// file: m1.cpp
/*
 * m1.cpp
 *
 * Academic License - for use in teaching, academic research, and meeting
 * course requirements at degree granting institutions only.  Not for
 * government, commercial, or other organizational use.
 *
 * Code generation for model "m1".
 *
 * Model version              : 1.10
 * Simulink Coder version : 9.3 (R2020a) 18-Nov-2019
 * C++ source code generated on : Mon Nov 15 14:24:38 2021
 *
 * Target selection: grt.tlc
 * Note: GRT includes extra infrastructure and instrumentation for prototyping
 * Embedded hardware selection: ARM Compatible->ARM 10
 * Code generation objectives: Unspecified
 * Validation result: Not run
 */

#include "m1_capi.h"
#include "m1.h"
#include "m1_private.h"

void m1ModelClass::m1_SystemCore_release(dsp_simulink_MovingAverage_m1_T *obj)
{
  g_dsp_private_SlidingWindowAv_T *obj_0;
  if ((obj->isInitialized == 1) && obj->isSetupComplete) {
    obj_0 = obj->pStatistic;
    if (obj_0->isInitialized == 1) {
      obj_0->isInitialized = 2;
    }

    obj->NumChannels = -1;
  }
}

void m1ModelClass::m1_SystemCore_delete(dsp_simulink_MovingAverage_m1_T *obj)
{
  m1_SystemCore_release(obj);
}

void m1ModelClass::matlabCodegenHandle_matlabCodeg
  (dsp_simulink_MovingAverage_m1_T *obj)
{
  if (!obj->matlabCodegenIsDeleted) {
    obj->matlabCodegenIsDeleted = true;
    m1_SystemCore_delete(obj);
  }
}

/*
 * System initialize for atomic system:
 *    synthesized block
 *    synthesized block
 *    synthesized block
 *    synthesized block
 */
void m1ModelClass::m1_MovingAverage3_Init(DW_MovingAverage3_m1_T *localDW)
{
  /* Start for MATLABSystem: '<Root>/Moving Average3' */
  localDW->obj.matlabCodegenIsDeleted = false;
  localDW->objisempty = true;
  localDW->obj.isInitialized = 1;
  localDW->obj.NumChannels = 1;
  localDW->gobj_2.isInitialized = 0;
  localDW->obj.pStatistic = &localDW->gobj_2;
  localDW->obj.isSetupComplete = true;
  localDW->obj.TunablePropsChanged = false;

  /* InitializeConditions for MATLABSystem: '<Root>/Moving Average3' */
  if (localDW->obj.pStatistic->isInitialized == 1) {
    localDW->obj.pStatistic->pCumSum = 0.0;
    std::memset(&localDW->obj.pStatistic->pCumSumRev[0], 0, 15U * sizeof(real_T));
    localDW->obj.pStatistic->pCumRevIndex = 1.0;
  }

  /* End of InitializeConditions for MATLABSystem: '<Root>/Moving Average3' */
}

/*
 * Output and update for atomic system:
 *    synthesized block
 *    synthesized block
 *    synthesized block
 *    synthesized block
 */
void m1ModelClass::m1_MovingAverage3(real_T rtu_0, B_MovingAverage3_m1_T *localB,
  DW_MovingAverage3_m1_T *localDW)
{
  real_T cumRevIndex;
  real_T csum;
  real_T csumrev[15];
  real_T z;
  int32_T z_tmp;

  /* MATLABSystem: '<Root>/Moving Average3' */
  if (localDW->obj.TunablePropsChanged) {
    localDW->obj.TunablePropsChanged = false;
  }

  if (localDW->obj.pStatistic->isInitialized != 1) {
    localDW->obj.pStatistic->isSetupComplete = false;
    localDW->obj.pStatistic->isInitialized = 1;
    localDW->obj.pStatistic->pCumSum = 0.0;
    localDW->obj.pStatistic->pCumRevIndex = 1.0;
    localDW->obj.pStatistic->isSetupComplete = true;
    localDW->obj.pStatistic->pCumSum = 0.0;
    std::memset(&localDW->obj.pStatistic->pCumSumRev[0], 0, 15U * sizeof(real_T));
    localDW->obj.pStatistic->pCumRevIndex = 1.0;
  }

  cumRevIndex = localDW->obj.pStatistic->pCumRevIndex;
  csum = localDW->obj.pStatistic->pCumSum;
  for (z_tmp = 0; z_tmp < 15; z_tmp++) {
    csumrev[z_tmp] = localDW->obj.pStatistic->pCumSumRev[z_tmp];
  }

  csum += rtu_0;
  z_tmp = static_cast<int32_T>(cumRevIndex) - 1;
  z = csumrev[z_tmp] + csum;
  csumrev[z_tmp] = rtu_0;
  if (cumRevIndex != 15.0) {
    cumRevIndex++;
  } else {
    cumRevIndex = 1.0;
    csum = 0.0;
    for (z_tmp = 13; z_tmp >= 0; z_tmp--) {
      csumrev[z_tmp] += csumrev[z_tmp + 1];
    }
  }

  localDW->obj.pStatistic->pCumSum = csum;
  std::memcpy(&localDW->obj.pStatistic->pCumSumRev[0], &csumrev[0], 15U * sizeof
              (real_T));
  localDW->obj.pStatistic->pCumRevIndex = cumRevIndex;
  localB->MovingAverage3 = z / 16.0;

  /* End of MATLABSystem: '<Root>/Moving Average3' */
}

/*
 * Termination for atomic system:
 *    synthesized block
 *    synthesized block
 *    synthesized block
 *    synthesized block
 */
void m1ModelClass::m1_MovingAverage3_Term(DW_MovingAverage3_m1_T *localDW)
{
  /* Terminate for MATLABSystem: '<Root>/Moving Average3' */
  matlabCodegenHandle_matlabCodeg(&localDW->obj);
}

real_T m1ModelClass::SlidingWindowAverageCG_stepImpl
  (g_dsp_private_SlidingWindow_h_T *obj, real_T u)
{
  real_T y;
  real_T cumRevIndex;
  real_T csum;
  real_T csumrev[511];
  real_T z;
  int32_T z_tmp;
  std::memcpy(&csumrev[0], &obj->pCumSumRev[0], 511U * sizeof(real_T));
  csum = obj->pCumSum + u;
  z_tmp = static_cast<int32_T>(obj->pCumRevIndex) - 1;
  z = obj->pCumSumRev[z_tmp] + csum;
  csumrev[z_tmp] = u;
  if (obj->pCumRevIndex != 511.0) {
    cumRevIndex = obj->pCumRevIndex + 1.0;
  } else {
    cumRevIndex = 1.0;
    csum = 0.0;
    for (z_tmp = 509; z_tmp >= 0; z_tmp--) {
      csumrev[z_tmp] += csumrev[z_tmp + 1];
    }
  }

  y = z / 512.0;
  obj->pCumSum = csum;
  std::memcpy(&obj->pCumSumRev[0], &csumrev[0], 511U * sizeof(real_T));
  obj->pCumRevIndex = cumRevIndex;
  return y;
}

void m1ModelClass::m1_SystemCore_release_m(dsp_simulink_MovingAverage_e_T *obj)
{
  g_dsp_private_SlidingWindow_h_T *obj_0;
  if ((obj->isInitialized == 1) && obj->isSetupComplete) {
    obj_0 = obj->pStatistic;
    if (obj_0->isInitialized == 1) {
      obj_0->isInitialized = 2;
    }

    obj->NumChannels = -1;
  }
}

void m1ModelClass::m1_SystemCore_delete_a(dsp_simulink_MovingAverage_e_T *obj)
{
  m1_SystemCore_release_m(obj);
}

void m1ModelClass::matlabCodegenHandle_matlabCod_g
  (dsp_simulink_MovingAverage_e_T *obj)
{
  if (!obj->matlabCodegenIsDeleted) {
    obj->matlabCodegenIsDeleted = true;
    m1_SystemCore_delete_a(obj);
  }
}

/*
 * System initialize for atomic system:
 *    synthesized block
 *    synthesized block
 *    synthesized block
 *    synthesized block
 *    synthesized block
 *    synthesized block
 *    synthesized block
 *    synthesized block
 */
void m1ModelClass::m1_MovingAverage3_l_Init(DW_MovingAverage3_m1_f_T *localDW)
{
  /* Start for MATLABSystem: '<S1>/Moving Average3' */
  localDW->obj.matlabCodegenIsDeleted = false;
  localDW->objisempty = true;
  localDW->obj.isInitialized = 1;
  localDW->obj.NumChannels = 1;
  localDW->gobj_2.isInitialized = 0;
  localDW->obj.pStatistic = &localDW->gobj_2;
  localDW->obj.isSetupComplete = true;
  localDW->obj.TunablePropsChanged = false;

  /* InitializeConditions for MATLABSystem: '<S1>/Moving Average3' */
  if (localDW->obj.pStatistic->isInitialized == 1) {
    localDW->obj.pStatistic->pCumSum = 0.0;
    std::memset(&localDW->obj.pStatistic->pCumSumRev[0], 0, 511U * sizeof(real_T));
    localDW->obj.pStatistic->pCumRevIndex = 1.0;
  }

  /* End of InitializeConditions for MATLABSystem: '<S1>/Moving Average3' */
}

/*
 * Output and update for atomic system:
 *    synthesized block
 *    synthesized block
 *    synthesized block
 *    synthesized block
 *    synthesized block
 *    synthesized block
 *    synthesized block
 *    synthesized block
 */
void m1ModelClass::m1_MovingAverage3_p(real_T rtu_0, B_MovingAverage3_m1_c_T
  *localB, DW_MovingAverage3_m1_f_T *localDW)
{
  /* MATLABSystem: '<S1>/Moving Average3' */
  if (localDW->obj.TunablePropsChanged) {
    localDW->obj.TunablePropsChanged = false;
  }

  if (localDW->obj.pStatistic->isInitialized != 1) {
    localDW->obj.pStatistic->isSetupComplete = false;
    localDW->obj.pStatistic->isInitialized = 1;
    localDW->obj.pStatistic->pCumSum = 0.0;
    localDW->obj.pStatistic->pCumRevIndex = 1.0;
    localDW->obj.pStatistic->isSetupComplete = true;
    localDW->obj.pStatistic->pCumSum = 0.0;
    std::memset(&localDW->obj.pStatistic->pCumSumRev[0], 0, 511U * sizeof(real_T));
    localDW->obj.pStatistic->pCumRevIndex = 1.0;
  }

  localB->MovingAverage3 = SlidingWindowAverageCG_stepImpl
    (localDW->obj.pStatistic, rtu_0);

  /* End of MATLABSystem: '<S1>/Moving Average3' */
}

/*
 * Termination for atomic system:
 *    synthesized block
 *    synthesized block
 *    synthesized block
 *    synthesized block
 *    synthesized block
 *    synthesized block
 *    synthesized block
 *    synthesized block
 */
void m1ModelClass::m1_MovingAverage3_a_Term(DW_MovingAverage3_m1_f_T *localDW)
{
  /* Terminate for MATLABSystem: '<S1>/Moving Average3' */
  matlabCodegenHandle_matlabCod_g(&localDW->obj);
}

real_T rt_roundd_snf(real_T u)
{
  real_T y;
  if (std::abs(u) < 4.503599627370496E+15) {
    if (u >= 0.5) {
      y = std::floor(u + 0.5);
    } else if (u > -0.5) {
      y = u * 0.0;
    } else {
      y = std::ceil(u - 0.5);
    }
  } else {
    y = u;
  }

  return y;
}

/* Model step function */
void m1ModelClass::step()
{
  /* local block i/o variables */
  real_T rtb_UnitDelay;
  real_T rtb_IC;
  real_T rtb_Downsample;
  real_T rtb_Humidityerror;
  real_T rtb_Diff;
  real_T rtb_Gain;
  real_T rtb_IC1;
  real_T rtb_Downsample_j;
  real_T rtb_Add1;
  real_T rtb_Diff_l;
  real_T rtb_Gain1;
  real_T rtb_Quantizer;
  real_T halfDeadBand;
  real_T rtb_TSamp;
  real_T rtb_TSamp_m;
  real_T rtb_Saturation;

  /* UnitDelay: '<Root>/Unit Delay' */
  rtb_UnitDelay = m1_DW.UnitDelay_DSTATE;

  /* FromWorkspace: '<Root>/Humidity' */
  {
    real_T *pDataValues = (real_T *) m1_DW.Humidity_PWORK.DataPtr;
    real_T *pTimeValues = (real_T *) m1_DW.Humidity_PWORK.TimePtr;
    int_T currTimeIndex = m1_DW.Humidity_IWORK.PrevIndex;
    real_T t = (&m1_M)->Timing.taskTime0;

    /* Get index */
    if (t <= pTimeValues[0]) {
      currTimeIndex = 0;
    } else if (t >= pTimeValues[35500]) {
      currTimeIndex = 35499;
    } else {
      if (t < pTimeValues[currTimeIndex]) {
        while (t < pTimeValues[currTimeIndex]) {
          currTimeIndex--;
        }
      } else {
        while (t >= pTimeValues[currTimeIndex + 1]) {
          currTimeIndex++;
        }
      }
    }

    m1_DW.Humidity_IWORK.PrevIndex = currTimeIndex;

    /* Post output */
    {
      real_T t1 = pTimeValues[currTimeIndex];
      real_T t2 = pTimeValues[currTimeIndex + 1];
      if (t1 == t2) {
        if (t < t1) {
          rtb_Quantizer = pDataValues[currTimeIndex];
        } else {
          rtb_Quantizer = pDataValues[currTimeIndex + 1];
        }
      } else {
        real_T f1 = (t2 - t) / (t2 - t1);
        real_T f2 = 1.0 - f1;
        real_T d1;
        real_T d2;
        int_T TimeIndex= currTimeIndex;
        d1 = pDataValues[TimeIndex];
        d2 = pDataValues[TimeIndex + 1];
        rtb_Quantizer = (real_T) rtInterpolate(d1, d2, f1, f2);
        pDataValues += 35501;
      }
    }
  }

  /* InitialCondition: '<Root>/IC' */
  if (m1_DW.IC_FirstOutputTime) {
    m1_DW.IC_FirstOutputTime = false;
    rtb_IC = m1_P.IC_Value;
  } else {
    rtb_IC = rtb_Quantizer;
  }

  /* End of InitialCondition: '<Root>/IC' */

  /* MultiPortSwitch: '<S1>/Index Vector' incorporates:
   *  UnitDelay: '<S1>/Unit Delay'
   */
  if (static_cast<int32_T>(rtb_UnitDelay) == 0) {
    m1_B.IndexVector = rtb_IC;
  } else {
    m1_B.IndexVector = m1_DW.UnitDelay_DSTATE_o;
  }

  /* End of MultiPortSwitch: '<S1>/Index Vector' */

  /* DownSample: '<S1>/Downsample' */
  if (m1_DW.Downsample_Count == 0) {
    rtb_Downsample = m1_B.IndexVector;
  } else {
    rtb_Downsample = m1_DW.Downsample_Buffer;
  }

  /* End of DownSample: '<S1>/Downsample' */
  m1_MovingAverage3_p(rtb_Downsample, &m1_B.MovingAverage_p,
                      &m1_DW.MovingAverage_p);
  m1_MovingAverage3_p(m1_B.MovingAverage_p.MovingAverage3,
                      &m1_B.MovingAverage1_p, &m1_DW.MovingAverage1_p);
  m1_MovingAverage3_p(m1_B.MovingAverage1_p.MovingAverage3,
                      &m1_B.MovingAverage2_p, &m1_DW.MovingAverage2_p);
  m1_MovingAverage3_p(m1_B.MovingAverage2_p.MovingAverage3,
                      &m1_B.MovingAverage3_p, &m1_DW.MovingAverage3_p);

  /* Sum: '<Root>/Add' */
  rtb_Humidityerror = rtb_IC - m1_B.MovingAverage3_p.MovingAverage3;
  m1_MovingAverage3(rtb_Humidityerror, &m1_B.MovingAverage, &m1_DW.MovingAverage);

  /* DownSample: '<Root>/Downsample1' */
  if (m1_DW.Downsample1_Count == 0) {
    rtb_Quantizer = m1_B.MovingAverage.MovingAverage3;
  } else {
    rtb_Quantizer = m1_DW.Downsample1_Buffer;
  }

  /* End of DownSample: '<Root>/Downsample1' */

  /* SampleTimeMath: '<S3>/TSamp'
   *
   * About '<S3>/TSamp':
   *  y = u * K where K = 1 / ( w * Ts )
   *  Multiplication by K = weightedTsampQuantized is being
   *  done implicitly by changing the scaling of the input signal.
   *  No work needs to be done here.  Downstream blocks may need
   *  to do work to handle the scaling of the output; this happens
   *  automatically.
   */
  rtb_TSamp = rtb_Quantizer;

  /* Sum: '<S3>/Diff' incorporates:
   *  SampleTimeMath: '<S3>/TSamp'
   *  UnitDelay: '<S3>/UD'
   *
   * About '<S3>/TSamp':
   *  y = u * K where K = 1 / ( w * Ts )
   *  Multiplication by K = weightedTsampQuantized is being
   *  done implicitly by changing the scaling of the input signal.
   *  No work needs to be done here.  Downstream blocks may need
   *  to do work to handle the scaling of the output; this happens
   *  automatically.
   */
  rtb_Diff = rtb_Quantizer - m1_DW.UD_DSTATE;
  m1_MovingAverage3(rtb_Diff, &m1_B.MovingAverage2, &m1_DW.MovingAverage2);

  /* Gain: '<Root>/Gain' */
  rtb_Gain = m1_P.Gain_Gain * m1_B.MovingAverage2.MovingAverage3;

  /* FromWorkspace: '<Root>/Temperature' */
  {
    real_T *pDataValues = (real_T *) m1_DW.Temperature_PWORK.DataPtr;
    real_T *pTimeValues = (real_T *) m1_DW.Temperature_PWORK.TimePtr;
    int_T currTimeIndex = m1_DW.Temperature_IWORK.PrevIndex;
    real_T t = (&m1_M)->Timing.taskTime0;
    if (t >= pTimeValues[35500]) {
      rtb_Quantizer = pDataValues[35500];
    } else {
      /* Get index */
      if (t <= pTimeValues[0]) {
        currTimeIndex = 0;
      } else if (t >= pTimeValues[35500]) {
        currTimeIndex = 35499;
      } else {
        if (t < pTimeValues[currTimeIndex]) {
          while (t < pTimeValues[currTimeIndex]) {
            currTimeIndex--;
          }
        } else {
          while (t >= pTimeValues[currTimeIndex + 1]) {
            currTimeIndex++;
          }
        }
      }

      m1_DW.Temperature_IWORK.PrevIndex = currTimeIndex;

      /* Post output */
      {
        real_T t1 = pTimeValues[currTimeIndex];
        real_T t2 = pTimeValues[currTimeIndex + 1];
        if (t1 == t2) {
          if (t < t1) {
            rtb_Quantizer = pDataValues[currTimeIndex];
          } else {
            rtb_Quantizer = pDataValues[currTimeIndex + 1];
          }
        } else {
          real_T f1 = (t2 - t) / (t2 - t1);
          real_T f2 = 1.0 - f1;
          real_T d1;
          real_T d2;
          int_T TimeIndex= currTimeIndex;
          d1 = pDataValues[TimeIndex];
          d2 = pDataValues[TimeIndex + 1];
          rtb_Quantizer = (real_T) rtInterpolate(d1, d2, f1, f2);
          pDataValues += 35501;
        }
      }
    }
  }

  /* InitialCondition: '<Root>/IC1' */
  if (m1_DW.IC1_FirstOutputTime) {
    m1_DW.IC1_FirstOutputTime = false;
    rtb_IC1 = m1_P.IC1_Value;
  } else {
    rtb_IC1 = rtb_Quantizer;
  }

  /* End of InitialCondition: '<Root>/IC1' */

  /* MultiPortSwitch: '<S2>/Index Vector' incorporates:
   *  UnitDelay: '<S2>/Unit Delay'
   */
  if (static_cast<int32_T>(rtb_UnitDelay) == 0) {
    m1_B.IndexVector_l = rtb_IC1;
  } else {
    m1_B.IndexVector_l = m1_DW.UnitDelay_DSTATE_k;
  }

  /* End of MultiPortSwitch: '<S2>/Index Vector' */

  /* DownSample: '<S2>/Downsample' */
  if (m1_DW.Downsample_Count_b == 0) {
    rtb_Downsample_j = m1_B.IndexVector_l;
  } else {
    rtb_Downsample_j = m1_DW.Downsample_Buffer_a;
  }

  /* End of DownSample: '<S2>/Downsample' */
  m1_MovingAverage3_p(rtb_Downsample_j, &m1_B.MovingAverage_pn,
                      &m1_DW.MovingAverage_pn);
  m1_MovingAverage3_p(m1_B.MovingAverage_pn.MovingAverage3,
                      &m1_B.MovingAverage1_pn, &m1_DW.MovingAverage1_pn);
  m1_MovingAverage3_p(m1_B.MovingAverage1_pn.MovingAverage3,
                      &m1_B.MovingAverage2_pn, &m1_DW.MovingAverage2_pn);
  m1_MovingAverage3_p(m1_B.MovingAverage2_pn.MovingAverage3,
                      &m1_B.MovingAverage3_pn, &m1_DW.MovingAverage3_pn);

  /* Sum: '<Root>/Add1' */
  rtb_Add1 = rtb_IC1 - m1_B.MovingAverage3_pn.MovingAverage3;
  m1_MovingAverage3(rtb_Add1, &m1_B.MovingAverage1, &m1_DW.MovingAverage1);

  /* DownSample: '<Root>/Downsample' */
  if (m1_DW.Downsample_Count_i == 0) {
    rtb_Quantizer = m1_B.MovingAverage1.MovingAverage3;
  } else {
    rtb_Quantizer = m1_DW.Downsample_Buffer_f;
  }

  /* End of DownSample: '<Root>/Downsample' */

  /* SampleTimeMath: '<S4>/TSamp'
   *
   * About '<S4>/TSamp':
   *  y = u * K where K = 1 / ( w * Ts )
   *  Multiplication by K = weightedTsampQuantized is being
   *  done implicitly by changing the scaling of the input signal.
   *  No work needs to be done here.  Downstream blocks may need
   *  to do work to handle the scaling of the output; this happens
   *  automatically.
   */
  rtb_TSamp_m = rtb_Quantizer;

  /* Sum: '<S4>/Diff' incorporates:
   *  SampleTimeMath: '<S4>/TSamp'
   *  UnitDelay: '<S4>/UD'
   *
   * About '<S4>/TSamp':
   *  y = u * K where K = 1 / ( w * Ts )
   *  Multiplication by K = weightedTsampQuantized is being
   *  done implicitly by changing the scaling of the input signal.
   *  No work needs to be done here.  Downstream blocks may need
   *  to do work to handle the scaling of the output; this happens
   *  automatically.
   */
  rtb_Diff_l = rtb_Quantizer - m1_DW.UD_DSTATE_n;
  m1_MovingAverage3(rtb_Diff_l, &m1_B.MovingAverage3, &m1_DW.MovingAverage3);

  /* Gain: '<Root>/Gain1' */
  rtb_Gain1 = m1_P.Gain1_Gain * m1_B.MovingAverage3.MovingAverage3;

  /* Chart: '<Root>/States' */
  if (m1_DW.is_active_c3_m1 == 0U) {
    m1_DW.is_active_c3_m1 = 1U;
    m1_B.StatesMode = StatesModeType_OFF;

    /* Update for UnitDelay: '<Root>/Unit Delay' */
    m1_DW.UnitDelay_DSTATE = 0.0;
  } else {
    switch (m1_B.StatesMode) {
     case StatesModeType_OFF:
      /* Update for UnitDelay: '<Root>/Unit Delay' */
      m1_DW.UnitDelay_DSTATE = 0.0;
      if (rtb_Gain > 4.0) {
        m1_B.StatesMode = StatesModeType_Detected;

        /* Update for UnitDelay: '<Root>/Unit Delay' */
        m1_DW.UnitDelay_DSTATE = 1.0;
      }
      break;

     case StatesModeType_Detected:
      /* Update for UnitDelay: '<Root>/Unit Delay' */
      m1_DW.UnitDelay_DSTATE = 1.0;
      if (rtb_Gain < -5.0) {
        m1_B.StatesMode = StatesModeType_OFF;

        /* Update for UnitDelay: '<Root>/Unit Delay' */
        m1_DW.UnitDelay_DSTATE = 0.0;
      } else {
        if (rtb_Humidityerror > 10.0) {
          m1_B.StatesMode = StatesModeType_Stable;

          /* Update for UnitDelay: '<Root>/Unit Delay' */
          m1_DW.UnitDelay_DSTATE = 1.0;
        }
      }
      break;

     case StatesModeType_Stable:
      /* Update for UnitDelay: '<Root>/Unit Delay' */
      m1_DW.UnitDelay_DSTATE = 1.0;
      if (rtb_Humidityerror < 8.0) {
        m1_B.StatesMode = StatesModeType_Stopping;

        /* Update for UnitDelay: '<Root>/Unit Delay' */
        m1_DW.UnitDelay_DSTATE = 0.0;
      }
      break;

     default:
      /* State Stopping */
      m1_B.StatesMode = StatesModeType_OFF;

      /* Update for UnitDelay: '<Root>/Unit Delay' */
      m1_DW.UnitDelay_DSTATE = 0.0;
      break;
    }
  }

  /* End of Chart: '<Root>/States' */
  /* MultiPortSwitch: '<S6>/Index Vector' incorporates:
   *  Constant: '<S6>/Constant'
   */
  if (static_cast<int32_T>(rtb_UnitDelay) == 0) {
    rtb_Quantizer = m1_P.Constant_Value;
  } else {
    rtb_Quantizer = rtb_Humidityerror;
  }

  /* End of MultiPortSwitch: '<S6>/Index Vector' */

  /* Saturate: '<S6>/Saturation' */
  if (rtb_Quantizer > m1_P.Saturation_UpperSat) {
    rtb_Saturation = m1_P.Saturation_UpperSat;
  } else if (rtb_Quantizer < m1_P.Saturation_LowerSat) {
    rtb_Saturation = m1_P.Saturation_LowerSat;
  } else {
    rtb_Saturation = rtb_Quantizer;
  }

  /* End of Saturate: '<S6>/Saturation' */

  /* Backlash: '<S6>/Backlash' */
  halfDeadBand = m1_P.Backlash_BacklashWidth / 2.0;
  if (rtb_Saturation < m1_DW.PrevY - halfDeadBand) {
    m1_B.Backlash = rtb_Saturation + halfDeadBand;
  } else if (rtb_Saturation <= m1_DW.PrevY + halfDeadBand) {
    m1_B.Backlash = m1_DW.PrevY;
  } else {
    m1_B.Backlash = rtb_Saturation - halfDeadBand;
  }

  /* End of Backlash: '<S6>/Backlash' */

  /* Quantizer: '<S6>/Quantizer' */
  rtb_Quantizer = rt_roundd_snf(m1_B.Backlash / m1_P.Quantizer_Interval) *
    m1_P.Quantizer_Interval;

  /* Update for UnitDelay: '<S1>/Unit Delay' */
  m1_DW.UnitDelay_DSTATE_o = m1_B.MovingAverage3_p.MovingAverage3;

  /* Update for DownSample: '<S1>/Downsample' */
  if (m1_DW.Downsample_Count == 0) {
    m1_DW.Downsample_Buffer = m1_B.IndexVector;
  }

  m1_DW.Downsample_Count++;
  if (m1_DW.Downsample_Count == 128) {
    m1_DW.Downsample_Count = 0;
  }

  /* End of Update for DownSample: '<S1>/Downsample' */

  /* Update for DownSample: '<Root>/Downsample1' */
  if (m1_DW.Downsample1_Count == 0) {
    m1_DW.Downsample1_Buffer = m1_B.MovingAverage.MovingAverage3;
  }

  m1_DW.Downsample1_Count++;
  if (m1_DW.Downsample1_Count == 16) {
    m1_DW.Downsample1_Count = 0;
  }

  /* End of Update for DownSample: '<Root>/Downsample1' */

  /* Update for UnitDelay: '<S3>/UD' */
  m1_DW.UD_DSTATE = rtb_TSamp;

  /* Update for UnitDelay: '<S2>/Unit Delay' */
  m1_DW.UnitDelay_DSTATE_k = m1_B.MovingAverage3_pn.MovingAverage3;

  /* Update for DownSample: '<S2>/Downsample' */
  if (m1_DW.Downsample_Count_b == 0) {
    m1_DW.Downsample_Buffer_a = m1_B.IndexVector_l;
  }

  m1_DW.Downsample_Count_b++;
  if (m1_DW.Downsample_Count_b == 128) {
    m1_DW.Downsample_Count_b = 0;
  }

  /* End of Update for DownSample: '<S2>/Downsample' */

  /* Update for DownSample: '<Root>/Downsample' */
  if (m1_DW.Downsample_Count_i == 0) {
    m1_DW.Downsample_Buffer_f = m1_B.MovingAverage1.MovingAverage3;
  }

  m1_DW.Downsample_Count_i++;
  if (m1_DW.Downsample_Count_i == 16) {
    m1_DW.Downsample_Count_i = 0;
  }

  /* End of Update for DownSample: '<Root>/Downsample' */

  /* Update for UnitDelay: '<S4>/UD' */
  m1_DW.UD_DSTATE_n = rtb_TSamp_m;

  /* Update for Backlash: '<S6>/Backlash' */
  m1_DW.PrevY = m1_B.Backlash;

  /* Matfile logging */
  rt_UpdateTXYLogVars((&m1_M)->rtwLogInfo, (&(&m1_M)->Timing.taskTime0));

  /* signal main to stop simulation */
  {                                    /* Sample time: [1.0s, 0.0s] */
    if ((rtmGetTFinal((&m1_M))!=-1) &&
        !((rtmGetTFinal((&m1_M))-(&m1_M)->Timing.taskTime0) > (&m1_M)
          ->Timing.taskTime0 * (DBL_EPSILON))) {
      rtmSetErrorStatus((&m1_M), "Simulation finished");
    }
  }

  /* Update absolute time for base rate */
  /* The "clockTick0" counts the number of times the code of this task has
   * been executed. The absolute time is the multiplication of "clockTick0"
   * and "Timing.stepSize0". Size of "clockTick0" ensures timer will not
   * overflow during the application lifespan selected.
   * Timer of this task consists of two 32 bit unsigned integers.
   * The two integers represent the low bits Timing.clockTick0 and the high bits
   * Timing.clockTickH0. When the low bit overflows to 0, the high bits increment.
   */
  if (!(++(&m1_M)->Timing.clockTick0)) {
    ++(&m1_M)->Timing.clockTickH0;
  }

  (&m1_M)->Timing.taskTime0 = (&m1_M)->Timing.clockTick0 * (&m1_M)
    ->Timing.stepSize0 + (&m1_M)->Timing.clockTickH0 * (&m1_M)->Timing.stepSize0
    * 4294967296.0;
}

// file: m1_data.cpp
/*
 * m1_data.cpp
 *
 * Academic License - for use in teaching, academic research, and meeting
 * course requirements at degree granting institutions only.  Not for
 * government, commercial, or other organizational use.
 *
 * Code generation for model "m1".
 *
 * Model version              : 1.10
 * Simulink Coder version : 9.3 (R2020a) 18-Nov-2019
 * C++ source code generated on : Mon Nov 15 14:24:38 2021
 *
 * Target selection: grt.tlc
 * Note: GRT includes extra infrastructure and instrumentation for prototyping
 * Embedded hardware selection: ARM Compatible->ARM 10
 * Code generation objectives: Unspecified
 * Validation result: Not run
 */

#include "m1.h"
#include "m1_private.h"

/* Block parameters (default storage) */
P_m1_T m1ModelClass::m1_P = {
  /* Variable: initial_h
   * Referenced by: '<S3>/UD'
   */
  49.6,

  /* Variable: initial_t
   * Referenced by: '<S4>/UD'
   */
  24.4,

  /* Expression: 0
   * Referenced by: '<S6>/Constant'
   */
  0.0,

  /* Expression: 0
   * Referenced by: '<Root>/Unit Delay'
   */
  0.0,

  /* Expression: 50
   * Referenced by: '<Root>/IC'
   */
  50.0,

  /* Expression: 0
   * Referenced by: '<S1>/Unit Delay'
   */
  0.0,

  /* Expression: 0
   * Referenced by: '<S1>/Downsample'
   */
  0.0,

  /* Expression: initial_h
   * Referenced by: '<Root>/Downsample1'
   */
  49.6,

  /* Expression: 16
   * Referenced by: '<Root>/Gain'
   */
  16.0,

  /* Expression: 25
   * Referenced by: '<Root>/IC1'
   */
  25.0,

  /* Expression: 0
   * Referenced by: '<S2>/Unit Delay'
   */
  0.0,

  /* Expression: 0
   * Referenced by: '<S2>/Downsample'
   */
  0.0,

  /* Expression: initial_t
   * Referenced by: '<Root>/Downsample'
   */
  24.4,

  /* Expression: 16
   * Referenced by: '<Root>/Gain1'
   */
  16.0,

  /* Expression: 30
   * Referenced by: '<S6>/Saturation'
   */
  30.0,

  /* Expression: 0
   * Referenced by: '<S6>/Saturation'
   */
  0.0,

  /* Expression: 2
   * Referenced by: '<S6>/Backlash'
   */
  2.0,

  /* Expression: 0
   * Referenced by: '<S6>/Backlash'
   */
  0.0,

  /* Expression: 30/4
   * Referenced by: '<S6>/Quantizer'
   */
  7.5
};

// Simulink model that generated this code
simulink model "m1"  (R2020a)
settings: Solver=FixedStepAuto  StartTime=0.0  StopTime=25000.0  FixedStep=1  RelTol=1e-3
libraries: dspstat3 x12, simulink x2

== system m1 ==
  Add : Sum  Inputs=-+
  Add1 : Sum  Inputs=-+
  Baseline predictor filter : Subsystem
  Baseline predictor filter1 : Subsystem
  Discrete Derivative : simulink/Discrete/Discrete Derivative  gainval=1.0  ICPrevScaledInput=initial_h  OutMin=[]  OutMax=[]  OutDataType=fixdt(1, 16)  OutScaling=2^-10  DoSatur=off
  Discrete Derivative1 : simulink/Discrete/Discrete Derivative  gainval=1.0  ICPrevScaledInput=initial_t  OutMin=[]  OutMax=[]  OutDataType=fixdt(1, 16)  OutScaling=2^-10  DoSatur=off
  Downsample : DownSample  N=16  phase=15  ic=initial_t
  Downsample1 : DownSample  N=16  phase=15  ic=initial_h
  Gain : Gain  Gain=16
  Gain1 : Gain  Gain=16
  Humidity : FromWorkspace  VariableName=TT_h1  OutDataTypeStr=double  SampleTime=-1
  IC : InitialCondition  Value=50
  IC1 : InitialCondition  Value=25
  Mode : Scope  NumInputPorts=2
  Moving Average{,1..3} (4 alike) : dspstat3/Moving Average  Method=Sliding window  ForgettingFactorPort=off  SpecifyWindowLength=on  WindowLength=16  ForgettingFactor=0.9  SimulateUsing=Code generation
  Output : Scope  NumInputPorts=3
  Scope humidity : Scope  NumInputPorts=3
  Scope temperature : Scope  NumInputPorts=3
  States : Stateflow chart  TreatAsAtomicUnit=on
  Temperature : FromWorkspace  VariableName=TT_t1  OutDataTypeStr=double  SampleTime=-1  OutputAfterFinalValue=Holding final value
  Unit Delay : UnitDelay  SampleTime=-1  HasFrameUpgradeWarning=on
  Vent power control : Subsystem
  wires:
  Humidity/1 -> IC/1
  Baseline predictor filter/1(Baseline) -> Scope humidity/2, Add/1
  Add/1 -> Vent power control/1(Humidity error), States/3(eH), Moving Average/1  "Humidity error"
  Temperature/1 -> IC1/1
  Add1/1 -> Moving Average1/1
  Discrete Derivative1/1 -> Moving Average3/1
  States/2(enabled) -> Unit Delay/1
  Unit Delay/1 -> Vent power control/2(Enabled), Baseline predictor filter1/2(Mode), Baseline predictor filter/2(Mode), Mode/1
  Downsample/1 -> Discrete Derivative1/1
  Downsample1/1 -> Discrete Derivative/1
  Baseline predictor filter1/1(Baseline) -> Add1/1, Scope temperature/2
  IC/1 -> Add/2, Baseline predictor filter/1(Measured value), Scope humidity/1
  IC1/1 -> Baseline predictor filter1/1(Measured value), Scope temperature/1, Add1/2
  Discrete Derivative/1 -> Moving Average2/1
  Moving Average/1 -> Downsample1/1
  Moving Average1/1 -> Downsample/1
  States/1(StatesMode) -> Mode/2
  Moving Average2/1 -> Gain/1
  Moving Average3/1 -> Gain1/1
  Gain/1 -> Scope humidity/3, States/1(dH)
  Gain1/1 -> Scope temperature/3, States/2(dT)
  Vent power control/1(Vent power level) -> Output/1

== system m1/Baseline predictor filter ==
  Measured value : Inport
  Mode : Inport  Port=2
  Downsample : DownSample  N=128
  Index Vector : MultiPortSwitch  DataPortOrder=Zero-based contiguous  Inputs=2  zeroidx=on
  Moving Average{,1..3} (4 alike) : dspstat3/Moving Average  Method=Sliding window  ForgettingFactorPort=off  SpecifyWindowLength=on  WindowLength=512  ForgettingFactor=0.9  SimulateUsing=Code generation
  Unit Delay : UnitDelay  SampleTime=-1  HasFrameUpgradeWarning=on
  Baseline : Outport
  wires:
  Moving Average1/1 -> Moving Average2/1
  Moving Average/1 -> Moving Average1/1
  Downsample/1 -> Moving Average/1
  Moving Average2/1 -> Moving Average3/1
  Index Vector/1 -> Downsample/1
  Mode/1 -> Index Vector/1
  Measured value/1 -> Index Vector/2
  Moving Average3/1 -> Unit Delay/1, Baseline/1
  Unit Delay/1 -> Index Vector/3

== system m1/Baseline predictor filter1 ==
  Measured value : Inport
  Mode : Inport  Port=2
  Downsample : DownSample  N=128
  Index Vector : MultiPortSwitch  DataPortOrder=Zero-based contiguous  Inputs=2  zeroidx=on
  Moving Average{,1..3} (4 alike) : dspstat3/Moving Average  Method=Sliding window  ForgettingFactorPort=off  SpecifyWindowLength=on  WindowLength=512  ForgettingFactor=0.9  SimulateUsing=Code generation
  Unit Delay : UnitDelay  SampleTime=-1  HasFrameUpgradeWarning=on
  Baseline : Outport
  wires:
  Unit Delay/1 -> Index Vector/3
  Index Vector/1 -> Downsample/1
  Moving Average3/1 -> Unit Delay/1, Baseline/1
  Measured value/1 -> Index Vector/2
  Mode/1 -> Index Vector/1
  Downsample/1 -> Moving Average/1
  Moving Average/1 -> Moving Average1/1
  Moving Average2/1 -> Moving Average3/1
  Moving Average1/1 -> Moving Average2/1

== system m1/Vent power control ==
  Humidity error : Inport
  Enabled : Inport  Port=2
  Backlash : Backlash  BacklashWidth=2
  Constant : Constant  Value=0
  Index Vector : MultiPortSwitch  DataPortOrder=Zero-based contiguous  Inputs=2  zeroidx=on
  Quantizer : Quantizer  QuantizationInterval=30/4  LinearizeAsGain=off
  Saturation : Saturate  UpperLimit=30  LowerLimit=0
  Vent power level : Outport
  wires:
  Constant/1 -> Index Vector/2
  Index Vector/1 -> Saturation/1  "Desired vent power"
  Humidity error/1 -> Index Vector/3
  Enabled/1 -> Index Vector/1
  Quantizer/1 -> Vent power level/1
  Saturation/1 -> Backlash/1
  Backlash/1 -> Quantizer/1

== stateflow chart m1/States ==
  state Stopping
    entry: enabled=0
  state Detected
    entry: enabled=1
  state Stable
    entry: enabled=1
  state OFF
    entry: enabled=0
  Stopping -> OFF
  Detected -> OFF [order 1] : [dH <  -5]
  Stable -> Stopping : [eH < 8]
  (default) -> OFF
  Detected -> Stable [order 2] : [eH > 10]
  OFF -> Detected : [dH > 4]
  data: dH input; dT input; StatesMode output Enum: StatesModeType; enabled output; eH input
